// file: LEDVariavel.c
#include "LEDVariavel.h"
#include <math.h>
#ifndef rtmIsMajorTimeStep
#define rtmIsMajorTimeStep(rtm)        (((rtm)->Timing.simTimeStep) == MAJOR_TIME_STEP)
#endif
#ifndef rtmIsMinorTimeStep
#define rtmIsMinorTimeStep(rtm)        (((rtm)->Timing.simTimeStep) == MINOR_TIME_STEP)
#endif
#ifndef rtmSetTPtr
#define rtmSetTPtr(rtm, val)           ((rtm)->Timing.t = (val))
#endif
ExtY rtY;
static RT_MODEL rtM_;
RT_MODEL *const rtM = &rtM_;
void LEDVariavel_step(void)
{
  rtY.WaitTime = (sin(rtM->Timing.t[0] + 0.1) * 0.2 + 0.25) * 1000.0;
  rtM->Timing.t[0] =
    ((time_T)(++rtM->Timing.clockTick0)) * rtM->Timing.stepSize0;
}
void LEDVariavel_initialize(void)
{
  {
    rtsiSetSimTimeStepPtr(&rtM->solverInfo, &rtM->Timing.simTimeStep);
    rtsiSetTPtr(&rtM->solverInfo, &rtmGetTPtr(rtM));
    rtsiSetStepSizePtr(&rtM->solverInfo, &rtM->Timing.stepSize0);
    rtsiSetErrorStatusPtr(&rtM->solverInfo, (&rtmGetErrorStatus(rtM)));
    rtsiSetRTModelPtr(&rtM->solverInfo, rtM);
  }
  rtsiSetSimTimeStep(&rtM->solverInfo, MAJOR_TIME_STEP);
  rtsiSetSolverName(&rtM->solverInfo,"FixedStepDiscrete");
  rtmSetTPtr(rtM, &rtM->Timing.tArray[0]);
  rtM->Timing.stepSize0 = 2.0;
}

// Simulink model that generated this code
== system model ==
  WaitTime : Outport  <- 1: Gain#1
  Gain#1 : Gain  Gain=1000  <- 1: Sin#1
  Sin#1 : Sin  Amplitude=0.2  Bias=0.25  Phase=0.1
